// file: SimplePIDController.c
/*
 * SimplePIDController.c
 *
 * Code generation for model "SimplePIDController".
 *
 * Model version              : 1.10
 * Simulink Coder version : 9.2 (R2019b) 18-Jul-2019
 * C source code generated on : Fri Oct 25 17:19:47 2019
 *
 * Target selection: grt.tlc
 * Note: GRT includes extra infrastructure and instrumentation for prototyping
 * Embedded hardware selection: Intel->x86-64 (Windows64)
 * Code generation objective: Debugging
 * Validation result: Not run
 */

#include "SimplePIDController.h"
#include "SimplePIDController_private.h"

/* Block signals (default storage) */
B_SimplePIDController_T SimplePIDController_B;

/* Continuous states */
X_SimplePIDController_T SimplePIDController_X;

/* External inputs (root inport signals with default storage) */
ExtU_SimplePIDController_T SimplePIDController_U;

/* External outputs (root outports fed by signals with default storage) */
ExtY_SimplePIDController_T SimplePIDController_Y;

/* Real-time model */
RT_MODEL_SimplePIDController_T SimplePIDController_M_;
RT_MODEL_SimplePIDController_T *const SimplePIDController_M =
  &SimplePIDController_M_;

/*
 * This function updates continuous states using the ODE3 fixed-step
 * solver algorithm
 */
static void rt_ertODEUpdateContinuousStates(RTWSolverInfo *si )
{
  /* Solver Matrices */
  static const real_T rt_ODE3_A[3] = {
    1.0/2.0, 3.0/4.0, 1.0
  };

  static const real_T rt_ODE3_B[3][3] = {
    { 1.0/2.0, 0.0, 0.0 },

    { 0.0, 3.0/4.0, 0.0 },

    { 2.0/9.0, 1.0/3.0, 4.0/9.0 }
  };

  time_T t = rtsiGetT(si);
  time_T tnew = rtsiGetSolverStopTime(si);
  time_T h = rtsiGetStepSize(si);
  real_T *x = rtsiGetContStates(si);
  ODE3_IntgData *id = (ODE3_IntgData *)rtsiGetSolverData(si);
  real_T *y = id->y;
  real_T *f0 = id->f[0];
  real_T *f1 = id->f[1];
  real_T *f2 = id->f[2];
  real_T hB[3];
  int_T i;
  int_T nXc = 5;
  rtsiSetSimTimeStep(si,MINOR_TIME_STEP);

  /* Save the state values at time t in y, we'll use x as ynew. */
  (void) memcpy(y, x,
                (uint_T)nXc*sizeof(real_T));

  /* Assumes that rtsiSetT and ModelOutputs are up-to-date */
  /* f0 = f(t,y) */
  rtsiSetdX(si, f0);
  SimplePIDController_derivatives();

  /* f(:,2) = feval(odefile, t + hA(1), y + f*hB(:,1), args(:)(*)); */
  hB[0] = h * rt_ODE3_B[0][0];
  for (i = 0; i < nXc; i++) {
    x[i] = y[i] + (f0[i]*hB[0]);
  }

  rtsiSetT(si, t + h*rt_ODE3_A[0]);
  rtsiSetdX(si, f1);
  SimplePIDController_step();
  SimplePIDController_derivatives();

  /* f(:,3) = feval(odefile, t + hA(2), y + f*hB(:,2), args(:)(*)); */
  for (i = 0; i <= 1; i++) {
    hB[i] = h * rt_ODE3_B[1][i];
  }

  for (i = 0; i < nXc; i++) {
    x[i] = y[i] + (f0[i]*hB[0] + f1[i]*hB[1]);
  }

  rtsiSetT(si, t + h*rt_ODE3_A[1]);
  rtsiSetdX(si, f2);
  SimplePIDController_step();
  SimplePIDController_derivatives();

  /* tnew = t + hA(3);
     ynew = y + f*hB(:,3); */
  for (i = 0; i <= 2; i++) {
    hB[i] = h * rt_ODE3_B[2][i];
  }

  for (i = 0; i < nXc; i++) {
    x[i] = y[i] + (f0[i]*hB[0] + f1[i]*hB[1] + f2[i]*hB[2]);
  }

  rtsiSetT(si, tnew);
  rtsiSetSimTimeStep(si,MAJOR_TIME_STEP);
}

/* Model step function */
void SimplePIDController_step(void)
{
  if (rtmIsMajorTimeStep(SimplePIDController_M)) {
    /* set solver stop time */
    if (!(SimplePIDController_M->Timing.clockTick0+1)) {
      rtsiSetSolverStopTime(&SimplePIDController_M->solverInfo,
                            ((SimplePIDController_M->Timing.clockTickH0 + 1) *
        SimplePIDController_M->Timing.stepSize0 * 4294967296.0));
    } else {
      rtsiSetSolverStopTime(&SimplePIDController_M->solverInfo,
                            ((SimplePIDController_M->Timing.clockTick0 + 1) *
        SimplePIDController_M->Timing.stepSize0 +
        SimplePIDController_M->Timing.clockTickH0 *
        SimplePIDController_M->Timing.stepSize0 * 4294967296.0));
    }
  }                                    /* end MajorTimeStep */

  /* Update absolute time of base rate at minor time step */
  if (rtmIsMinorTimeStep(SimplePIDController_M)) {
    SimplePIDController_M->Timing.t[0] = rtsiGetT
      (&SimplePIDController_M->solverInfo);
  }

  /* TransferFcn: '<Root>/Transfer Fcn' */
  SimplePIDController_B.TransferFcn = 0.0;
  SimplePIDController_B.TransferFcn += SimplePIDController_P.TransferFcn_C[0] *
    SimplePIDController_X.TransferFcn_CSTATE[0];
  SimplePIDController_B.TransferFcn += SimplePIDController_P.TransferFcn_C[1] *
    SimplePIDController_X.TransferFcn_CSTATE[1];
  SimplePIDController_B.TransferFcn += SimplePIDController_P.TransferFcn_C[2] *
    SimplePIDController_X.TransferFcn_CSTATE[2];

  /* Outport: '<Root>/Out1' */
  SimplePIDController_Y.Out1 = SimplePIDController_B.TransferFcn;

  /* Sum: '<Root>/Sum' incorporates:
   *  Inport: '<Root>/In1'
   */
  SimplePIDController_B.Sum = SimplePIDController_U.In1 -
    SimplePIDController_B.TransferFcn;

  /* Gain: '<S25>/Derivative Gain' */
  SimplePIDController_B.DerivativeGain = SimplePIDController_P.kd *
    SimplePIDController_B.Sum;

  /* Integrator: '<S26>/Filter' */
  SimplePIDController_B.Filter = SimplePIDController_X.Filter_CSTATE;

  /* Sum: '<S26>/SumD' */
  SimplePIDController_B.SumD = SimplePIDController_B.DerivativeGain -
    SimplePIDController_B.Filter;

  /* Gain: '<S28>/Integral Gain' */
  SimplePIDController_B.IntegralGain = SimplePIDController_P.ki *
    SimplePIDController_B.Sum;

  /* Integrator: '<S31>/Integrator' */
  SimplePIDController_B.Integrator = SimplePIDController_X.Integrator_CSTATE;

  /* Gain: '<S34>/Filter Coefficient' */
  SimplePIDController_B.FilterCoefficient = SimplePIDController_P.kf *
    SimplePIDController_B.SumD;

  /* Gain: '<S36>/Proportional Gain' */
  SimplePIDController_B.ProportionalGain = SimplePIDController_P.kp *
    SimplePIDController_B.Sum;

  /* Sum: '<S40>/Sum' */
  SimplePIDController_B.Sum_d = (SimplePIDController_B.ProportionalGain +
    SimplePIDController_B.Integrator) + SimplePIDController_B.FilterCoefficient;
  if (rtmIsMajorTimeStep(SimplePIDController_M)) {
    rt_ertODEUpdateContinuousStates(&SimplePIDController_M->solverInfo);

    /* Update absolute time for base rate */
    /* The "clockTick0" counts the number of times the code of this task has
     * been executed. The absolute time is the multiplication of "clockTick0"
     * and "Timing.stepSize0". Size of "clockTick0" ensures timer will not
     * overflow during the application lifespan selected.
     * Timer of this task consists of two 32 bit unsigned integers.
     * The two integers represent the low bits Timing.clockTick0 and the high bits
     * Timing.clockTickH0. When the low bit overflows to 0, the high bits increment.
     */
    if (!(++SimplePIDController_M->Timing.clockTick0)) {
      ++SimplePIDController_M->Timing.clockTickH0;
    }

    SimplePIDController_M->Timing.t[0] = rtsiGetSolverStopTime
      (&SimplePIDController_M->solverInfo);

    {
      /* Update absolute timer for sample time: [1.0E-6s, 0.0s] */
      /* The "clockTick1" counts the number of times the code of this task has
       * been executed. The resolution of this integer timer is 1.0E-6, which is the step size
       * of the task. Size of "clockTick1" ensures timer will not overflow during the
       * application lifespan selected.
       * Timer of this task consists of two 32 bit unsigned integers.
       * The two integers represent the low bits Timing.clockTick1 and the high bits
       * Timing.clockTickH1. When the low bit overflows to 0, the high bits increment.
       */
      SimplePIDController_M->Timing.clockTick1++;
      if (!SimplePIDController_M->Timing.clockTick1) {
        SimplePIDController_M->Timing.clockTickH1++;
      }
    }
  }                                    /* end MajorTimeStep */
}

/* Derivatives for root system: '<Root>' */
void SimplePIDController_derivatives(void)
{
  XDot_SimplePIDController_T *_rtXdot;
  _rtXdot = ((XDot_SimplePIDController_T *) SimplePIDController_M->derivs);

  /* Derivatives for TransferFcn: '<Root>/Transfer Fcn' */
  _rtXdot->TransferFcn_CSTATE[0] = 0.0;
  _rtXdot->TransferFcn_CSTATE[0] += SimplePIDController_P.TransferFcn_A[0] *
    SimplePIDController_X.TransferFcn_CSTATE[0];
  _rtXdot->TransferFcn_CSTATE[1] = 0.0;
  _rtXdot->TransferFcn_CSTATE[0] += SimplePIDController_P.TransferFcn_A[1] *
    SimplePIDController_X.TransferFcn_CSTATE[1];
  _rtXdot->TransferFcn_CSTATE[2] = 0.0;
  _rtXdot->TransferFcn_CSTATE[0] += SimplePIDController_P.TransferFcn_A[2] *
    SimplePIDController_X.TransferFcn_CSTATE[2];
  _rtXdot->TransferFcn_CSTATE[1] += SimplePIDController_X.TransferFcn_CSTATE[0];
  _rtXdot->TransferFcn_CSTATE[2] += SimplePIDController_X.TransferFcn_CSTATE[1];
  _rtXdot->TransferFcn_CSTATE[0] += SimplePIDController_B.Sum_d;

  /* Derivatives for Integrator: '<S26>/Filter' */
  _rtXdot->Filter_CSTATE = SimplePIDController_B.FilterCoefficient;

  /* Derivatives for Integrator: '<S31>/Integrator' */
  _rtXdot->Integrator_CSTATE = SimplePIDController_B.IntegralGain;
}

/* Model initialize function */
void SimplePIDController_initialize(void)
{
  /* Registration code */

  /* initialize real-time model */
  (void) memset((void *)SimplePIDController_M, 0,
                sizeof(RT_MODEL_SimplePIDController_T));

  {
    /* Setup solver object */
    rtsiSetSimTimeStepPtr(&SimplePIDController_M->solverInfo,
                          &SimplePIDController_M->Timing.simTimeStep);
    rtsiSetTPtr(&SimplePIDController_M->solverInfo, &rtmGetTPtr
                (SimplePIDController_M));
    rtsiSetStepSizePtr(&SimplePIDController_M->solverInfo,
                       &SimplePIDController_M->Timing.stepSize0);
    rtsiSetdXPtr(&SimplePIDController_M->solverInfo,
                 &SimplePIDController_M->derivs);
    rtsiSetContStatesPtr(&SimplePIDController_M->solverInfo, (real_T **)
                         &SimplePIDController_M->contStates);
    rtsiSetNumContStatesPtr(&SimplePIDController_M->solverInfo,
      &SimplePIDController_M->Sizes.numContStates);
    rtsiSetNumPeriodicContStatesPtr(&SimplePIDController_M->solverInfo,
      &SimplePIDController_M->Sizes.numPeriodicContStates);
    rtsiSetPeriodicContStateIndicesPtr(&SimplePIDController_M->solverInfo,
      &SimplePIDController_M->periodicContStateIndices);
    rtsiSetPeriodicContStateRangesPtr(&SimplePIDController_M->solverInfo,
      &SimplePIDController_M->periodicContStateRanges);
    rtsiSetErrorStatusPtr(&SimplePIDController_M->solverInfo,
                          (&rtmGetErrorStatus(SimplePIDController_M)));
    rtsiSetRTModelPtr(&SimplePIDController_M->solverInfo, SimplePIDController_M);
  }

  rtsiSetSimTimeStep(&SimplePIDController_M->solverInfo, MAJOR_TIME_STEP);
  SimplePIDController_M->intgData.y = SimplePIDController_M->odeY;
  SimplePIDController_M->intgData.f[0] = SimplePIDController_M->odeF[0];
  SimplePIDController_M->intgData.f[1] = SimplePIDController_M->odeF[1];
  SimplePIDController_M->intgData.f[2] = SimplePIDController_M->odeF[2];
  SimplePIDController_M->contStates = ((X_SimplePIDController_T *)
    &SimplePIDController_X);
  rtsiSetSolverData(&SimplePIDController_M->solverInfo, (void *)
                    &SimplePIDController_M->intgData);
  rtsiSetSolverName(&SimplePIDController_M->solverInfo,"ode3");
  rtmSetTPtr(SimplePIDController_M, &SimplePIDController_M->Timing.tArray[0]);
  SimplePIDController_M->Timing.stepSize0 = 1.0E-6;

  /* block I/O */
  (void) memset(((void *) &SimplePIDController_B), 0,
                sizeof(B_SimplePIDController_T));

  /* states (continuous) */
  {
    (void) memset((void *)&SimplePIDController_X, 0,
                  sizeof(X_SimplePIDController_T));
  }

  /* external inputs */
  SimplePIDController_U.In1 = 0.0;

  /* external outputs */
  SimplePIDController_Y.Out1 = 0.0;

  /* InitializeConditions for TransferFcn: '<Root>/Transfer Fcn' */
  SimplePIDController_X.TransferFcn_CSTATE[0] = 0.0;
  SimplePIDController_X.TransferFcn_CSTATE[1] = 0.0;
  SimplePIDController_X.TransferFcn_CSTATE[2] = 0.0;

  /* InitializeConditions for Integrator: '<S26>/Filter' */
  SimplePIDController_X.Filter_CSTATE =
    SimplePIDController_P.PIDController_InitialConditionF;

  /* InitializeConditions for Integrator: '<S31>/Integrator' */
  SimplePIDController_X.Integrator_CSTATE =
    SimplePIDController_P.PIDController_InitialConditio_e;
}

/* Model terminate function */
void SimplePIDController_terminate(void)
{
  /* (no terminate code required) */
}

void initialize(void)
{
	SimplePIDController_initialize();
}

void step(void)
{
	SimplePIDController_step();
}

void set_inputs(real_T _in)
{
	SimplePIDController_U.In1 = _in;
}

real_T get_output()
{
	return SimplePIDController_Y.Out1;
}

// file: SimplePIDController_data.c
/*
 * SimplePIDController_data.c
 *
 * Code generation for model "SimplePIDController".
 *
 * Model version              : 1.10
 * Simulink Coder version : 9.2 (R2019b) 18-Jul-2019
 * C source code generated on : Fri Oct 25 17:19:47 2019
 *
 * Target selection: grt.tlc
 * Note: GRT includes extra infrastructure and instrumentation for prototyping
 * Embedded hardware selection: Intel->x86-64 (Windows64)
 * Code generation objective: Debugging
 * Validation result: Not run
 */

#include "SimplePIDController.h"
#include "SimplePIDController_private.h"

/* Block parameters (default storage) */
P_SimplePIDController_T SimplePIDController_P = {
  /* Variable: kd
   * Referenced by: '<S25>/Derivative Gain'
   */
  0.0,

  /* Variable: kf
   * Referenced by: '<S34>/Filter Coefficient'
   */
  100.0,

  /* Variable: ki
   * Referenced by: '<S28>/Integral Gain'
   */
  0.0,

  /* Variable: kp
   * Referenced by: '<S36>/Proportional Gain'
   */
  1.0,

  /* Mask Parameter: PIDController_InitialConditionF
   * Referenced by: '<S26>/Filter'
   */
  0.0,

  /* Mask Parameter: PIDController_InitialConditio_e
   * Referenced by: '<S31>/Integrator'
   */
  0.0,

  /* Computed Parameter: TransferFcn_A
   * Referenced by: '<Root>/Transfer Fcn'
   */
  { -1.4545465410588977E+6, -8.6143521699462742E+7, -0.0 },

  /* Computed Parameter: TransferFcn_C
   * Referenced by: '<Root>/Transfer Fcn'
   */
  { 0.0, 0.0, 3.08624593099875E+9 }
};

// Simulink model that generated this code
simulink model "SimplePIDController"  (R2019b)
settings: Solver=FixedStepAuto  StartTime=0.0  StopTime=1  FixedStep=0.000001  RelTol=1e-3
values from neighbouring files (symbols this model uses):
  b = 3.5077e-06    [params.mat]
  J = 3.2284e-06    [params.mat]
  K = 0.0274    [params.mat]
  kd = 0    [params.mat]
  kf = 100    [params.mat]
  ki = 0    [params.mat]
  kp = 1    [params.mat]
  L = 2.75e-06    [params.mat]
  R = 4    [params.mat]
libraries: simulink x1

== system SimplePIDController ==
  In1 : Inport  OutDataTypeStr=double
  PID Controller : simulink/Continuous/PID Controller  Controller=PID  Form=Parallel  TimeDomain=Continuous-time  SampleTime=-1  IntegratorMethod=Forward Euler  FilterMethod=Forward Euler  ControllerParametersSource=internal  P=kp  I=ki  D=kd  UseFilter=on  N=kf  TunerSelectOption=Transfer Function Based (PID Tuner App)  InitialConditionSource=internal  InitialConditionForIntegrator=0  InitialConditionForFilter=0  DifferentiatorICPrevScaledInput=0  ExternalReset=none  TrackingMode=off  Kt=1  LimitOutput=off  UpperSaturationLimit=inf  LowerSaturationLimit=-inf  LinearizeAsGain=on  AntiWindupMode=none  Kb=1  PGainOutDataTypeStr=double  PProdOutDataTypeStr=double  POutMin=[]  POutMax=[]  IGainOutDataTypeStr=double  IProdOutDataTypeStr=double  IOutMin=[]  IOutMax=[]  DGainOutDataTypeStr=double  DProdOutDataTypeStr=double  DOutMin=[]  DOutMax=[]  NGainOutDataTypeStr=double  NProdOutDataTypeStr=double  NOutMin=[]  NOutMax=[]  SumOutDataTypeStr=double  SumOutMin=[]  SumOutMax=[]  SaturationOutMin=[]  SaturationOutMax=[]  PParamDataTypeStr=double  PParamMin=[]  PParamMax=[]  IParamDataTypeStr=double  IParamMin=[]  IParamMax=[]  DParamDataTypeStr=double  DParamMin=[]  DParamMax=[]  NParamDataTypeStr=double  NParamMin=[]  NParamMax=[]  KbParamMin=[]  KbParamMax=[]  KtParamMin=[]  KtParamMax=[]  KbOutMin=[]  KbOutMax=[]  KtOutMin=[]  KtOutMax=[]  IntegratorOutMin=[]  IntegratorOutMax=[]  FilterOutMin=[]  FilterOutMax=[]  SumI1OutMin=[]  SumI1OutMax=[]  SumI2OutMin=[]  SumI2OutMax=[]  SumI3OutMin=[]  SumI3OutMax=[]  SumI4OutMin=[]  SumI4OutMax=[]  SumDOutDataTypeStr=double  SumDOutMin=[]  SumDOutMax=[]  SumAccumDataTypeStr=double  SumDAccumDataTypeStr=double  DifferentiatorOutMin=[]  DifferentiatorOutMax=[]  FilterDiffOutCoefMin=[]  FilterDiffOutCoefMax=[]  ReciprocalOutMin=[]  ReciprocalOutMax=[]  SumDenOutMin=[]  SumDenOutMax=[]  SumNumOutMin=[]  SumNumOutMax=[]  DivideOutMin=[]  DivideOutMax=[]  IntegratorContinuousStateAttributes=''  IntegratorStateMustResolveToSignalObject=off  IntegratorRTWStateStorageClass=Auto  FilterContinuousStateAttributes=''  FilterStateMustResolveToSignalObject=off  FilterRTWStateStorageClass=Auto  ParallelPVariant=InternalParameters  IdealPVariant=Disabled  IVariant=InternalParameters  DVariant=InternalParameters  IntegratorVariant=Continuous  SatVariant=Disabled  AWVariant=Passthrough  PCopyVariant=Disabled  TRVariant=Disabled  FdbkBlocksVariant=Forward  IdealPFdbkVariant=Disabled  SatFdbkVariant=Disabled  DerivativeFilterVariant=ContFilter  NVariant=InternalParameters  NCopyVariant=Disabled  FilterICVariant=InternalICsFilter  IntegratorICVariant=InternalICs  ExternalResetVariant=Disabled  TRSumVariant=Passthrough  SumFdbkVariant=Disabled  SumVariant=Sum_PID
  Sum : Sum  Inputs=|+-  AccumDataTypeStr=double  OutDataTypeStr=double  InputSameDT=on
  Transfer Fcn : TransferFcn  Numerator=[K]  Denominator=[J*L J*R+b*L b*R+K*K 0]
  Out1 : Outport  OutDataTypeStr=double
  wires:
  PID Controller/1 -> Transfer Fcn/1
  Sum/1 -> PID Controller/1
  Transfer Fcn/1 -> Sum/2, Out1/1
  In1/1 -> Sum/1
